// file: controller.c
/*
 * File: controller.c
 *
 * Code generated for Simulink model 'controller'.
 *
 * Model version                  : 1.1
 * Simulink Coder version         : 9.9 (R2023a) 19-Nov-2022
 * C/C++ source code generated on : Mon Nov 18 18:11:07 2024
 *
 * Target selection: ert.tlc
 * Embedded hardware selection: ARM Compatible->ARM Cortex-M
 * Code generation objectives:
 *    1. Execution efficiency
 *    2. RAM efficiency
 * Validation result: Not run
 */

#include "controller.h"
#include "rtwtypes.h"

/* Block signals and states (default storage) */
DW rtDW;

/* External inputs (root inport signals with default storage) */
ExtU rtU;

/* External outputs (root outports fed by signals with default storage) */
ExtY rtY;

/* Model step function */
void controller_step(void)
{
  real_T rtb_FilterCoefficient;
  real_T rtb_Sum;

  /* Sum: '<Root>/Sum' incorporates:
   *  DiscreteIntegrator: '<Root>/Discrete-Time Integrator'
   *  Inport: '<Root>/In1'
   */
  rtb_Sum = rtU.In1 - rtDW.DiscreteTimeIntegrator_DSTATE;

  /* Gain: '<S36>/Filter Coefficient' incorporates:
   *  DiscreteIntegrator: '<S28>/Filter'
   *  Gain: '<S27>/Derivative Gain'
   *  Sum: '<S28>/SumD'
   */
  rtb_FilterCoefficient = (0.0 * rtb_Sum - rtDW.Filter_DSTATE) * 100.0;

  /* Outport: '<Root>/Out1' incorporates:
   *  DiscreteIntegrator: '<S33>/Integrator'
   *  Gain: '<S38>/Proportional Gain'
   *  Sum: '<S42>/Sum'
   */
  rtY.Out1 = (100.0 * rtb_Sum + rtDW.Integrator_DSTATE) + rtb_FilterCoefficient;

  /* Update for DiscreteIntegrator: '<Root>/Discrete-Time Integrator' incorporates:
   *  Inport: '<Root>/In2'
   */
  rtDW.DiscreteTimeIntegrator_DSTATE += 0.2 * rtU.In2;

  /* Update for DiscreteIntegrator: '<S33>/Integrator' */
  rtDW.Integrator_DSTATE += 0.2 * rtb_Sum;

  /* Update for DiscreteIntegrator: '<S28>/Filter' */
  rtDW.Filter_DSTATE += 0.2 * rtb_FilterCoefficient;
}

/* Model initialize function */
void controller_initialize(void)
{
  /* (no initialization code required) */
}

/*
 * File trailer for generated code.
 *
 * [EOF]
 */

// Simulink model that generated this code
simulink model "controller"  (R2023a)
settings: Solver=VariableStepAuto  StartTime=0.0  StopTime=10.0  RelTol=1e-3
undefined symbols (not defined in the file or in its folder): DiscIntNeverNeededParam
libraries: slpidlib x1

== system controller ==
  In1 : Inport
  In2 : Inport  Port=2
  Discrete PID Controller : slpidlib/PID Controller  Controller=PID  Form=Parallel  TimeDomain=Discrete-time  UseExternalTs=off  SampleTime=-1  IntegratorMethod=Forward Euler  FilterMethod=Forward Euler  ControllerParametersSource=internal  P=100  I=1  UseKiTs=off  D=0  N=100  UseFilter=on  TunerSelectOption=Transfer Function Based (PID Tuner App)  InitialConditionSource=internal  InitialConditionForIntegrator=0  InitialConditionForFilter=0  DifferentiatorICPrevScaledInput=0  ExternalReset=none  TrackingMode=off  Kt=1  LimitOutput=off  SatLimitsSource=internal  UpperSaturationLimit=inf  LowerSaturationLimit=-inf  LinearizeAsGain=off  AntiWindupMode=none  Kb=1  LimitIntegrator=off  UpperIntegratorSaturationLimit=inf  LowerIntegratorSaturationLimit=-inf  POutMin=[]  POutMax=[]  IOutMin=[]  IOutMax=[]  DOutMin=[]  DOutMax=[]  NOutMin=[]  NOutMax=[]  SumOutMin=[]  SumOutMax=[]  SaturationOutMin=[]  SaturationOutMax=[]  PParamMin=[]  PParamMax=[]  IParamMin=[]  IParamMax=[]  DParamMin=[]  DParamMax=[]  NParamMin=[]  NParamMax=[]  KbParamMin=[]  KbParamMax=[]  KtParamMin=[]  KtParamMax=[]  KbOutMin=[]  KbOutMax=[]  KtOutMin=[]  KtOutMax=[]  IntegratorOutMin=[]  IntegratorOutMax=[]  FilterOutMin=[]  FilterOutMax=[]  SumI1OutMin=[]  SumI1OutMax=[]  SumI2OutMin=[]  SumI2OutMax=[]  SumI3OutMin=[]  SumI3OutMax=[]  SumI4OutMin=[]  SumI4OutMax=[]  SumDOutMin=[]  SumDOutMax=[]  DifferentiatorOutMin=[]  DifferentiatorOutMax=[]  FilterDiffOutCoefMin=[]  FilterDiffOutCoefMax=[]  ReciprocalOutMin=[]  ReciprocalOutMax=[]  SumDenOutMin=[]  SumDenOutMax=[]  SumNumOutMin=[]  SumNumOutMax=[]  DivideOutMin=[]  DivideOutMax=[]  UdiffTsProdOutMin=[]  UdiffTsProdOutMax=[]  NTsProdOutMin=[]  NTsProdOutMax=[]  UintegralTsProdOutMin=[]  UintegralTsProdOutMax=[]  UngainTsProdOutMin=[]  UngainTsProdOutMax=[]  ClampingZeroOutDataTypeStr=Inherit: Inherit via back propagation  ClampingZeroOutMin=[]  ClampingZeroOutMax=[]  FilterDenConstantOutDataTypeStr=Inherit: Inherit via back propagation  FilterDenConstantOutMin=[]  FilterDenConstantOutMax=[]  PCopyOutDataTypeStr=Inherit: Inherit via back propagation  PCopyOutMin=[]  PCopyOutMax=[]  NCopyOutDataTypeStr=Inherit: Inherit via back propagation  NCopyOutMin=[]  NCopyOutMax=[]  IntegratorContinuousStateAttributes=''  IntegratorStateMustResolveToSignalObject=off  IntegratorRTWStateStorageClass=Auto  FilterContinuousStateAttributes=''  FilterStateMustResolveToSignalObject=off  FilterRTWStateStorageClass=Auto  ParallelPVariant=InternalParameters  IdealPVariant=Disabled  IVariant=InternalParameters  DVariant=InternalParameters  IntegratorVariant=Discrete  SatVariant=Disabled  AWVariant=Passthrough  PCopyVariant=Disabled  TRVariant=Disabled  FdbkBlocksVariant=Forward  IdealPFdbkVariant=Disabled  SatFdbkVariant=Disabled  DerivativeFilterVariant=ForwardEulerFilter  NVariant=InternalParameters  NCopyVariant=Disabled  FilterICVariant=InternalICsFilter  IntegratorICVariant=InternalICs  ExternalResetVariant=Disabled  TRSumVariant=Passthrough  SumFdbkVariant=Disabled  SumVariant=Sum_PID  TsampFilterVariant=InternalTs  TsampNgainVariant=Passthrough  TsampIntegralVariant=Disabled_SignalSpec  ExternalSaturationOutDataTypeStr=Inherit: Same as second input
  Discrete-Time Integrator : DiscreteIntegrator  SampleTime=-1  ICPrevOutput=DiscIntNeverNeededParam  ICPrevScaledInput=DiscIntNeverNeededParam
  Sum : Sum  Inputs=|+-
  Out1 : Outport
  wires:
  In2/1 -> Discrete-Time Integrator/1
  In1/1 -> Sum/1
  Discrete-Time Integrator/1 -> Sum/2
  Sum/1 -> Discrete PID Controller/1
  Discrete PID Controller/1 -> Out1/1
